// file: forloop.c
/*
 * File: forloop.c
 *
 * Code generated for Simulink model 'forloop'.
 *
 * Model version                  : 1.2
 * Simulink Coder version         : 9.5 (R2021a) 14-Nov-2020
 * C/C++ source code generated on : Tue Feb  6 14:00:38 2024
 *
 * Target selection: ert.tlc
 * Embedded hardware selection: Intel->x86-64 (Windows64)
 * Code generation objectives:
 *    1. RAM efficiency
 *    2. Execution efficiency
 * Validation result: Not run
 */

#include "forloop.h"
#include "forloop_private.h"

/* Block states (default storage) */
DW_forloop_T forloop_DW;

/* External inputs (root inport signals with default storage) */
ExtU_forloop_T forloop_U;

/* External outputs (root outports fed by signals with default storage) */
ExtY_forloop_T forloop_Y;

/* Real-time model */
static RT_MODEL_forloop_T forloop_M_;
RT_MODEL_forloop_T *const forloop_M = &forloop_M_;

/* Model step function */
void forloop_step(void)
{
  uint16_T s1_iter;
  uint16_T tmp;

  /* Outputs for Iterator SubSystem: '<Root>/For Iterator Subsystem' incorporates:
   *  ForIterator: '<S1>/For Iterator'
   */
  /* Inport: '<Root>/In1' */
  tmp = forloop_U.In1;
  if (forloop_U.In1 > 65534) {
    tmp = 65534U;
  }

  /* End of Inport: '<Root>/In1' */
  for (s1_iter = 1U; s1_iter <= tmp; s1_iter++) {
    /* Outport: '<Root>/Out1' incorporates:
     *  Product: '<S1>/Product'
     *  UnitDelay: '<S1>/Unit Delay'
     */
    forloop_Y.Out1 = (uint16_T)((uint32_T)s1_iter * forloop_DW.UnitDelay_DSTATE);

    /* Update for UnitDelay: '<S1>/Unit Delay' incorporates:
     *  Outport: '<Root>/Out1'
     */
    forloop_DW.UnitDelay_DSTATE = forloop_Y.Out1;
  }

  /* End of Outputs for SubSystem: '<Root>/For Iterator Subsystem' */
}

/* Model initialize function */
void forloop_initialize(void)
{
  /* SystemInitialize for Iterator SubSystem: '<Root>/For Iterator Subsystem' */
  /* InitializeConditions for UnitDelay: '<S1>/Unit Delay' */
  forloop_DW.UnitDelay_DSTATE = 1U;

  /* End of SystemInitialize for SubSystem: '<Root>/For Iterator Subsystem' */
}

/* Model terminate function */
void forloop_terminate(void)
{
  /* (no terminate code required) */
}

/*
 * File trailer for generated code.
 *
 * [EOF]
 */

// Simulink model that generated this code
simulink model "forloop"  (R2021a)
settings: Solver=FixedStepDiscrete  StartTime=0.0  StopTime=10.0  RelTol=1e-3

== system forloop ==
  In1 : Inport
  Constant : Constant  Value=5  OutDataTypeStr=uint16
  Display : Display
  For Iterator Subsystem : Subsystem  TreatAsAtomicUnit=on
  For Iterator Subsystem1 : Subsystem  TreatAsAtomicUnit=on
  Out1 : Outport
  wires:
  In1/1 -> For Iterator Subsystem/1(In1)
  For Iterator Subsystem/1(Out1) -> Out1/1
  Constant/1 -> For Iterator Subsystem1/1(In1)
  For Iterator Subsystem1/1(Out1) -> Display/1

== system forloop/For Iterator Subsystem ==
  In1 : Inport  OutDataTypeStr=uint16
  For Iterator : ForIterator  IterationSource=external  IterationVariableDataType=uint16
  Product : Product  OutDataTypeStr=uint16
  Unit Delay : UnitDelay  InitialCondition=1  SampleTime=-1  HasFrameUpgradeWarning=on
  Out1 : Outport  OutDataTypeStr=uint16
  wires:
  In1/1 -> For Iterator/1
  Product/1 -> Unit Delay/1, Out1/1
  For Iterator/1 -> Product/1
  Unit Delay/1 -> Product/2

== system forloop/For Iterator Subsystem1 ==
  In1 : Inport  OutDataTypeStr=uint16
  For Iterator : ForIterator  IterationSource=external  IterationVariableDataType=uint16
  Product : Product  OutDataTypeStr=uint16
  Unit Delay : UnitDelay  InitialCondition=1  SampleTime=-1  HasFrameUpgradeWarning=on
  Out1 : Outport  OutDataTypeStr=uint16
  wires:
  In1/1 -> For Iterator/1
  Product/1 -> Unit Delay/1, Out1/1
  For Iterator/1 -> Product/1
  Unit Delay/1 -> Product/2
